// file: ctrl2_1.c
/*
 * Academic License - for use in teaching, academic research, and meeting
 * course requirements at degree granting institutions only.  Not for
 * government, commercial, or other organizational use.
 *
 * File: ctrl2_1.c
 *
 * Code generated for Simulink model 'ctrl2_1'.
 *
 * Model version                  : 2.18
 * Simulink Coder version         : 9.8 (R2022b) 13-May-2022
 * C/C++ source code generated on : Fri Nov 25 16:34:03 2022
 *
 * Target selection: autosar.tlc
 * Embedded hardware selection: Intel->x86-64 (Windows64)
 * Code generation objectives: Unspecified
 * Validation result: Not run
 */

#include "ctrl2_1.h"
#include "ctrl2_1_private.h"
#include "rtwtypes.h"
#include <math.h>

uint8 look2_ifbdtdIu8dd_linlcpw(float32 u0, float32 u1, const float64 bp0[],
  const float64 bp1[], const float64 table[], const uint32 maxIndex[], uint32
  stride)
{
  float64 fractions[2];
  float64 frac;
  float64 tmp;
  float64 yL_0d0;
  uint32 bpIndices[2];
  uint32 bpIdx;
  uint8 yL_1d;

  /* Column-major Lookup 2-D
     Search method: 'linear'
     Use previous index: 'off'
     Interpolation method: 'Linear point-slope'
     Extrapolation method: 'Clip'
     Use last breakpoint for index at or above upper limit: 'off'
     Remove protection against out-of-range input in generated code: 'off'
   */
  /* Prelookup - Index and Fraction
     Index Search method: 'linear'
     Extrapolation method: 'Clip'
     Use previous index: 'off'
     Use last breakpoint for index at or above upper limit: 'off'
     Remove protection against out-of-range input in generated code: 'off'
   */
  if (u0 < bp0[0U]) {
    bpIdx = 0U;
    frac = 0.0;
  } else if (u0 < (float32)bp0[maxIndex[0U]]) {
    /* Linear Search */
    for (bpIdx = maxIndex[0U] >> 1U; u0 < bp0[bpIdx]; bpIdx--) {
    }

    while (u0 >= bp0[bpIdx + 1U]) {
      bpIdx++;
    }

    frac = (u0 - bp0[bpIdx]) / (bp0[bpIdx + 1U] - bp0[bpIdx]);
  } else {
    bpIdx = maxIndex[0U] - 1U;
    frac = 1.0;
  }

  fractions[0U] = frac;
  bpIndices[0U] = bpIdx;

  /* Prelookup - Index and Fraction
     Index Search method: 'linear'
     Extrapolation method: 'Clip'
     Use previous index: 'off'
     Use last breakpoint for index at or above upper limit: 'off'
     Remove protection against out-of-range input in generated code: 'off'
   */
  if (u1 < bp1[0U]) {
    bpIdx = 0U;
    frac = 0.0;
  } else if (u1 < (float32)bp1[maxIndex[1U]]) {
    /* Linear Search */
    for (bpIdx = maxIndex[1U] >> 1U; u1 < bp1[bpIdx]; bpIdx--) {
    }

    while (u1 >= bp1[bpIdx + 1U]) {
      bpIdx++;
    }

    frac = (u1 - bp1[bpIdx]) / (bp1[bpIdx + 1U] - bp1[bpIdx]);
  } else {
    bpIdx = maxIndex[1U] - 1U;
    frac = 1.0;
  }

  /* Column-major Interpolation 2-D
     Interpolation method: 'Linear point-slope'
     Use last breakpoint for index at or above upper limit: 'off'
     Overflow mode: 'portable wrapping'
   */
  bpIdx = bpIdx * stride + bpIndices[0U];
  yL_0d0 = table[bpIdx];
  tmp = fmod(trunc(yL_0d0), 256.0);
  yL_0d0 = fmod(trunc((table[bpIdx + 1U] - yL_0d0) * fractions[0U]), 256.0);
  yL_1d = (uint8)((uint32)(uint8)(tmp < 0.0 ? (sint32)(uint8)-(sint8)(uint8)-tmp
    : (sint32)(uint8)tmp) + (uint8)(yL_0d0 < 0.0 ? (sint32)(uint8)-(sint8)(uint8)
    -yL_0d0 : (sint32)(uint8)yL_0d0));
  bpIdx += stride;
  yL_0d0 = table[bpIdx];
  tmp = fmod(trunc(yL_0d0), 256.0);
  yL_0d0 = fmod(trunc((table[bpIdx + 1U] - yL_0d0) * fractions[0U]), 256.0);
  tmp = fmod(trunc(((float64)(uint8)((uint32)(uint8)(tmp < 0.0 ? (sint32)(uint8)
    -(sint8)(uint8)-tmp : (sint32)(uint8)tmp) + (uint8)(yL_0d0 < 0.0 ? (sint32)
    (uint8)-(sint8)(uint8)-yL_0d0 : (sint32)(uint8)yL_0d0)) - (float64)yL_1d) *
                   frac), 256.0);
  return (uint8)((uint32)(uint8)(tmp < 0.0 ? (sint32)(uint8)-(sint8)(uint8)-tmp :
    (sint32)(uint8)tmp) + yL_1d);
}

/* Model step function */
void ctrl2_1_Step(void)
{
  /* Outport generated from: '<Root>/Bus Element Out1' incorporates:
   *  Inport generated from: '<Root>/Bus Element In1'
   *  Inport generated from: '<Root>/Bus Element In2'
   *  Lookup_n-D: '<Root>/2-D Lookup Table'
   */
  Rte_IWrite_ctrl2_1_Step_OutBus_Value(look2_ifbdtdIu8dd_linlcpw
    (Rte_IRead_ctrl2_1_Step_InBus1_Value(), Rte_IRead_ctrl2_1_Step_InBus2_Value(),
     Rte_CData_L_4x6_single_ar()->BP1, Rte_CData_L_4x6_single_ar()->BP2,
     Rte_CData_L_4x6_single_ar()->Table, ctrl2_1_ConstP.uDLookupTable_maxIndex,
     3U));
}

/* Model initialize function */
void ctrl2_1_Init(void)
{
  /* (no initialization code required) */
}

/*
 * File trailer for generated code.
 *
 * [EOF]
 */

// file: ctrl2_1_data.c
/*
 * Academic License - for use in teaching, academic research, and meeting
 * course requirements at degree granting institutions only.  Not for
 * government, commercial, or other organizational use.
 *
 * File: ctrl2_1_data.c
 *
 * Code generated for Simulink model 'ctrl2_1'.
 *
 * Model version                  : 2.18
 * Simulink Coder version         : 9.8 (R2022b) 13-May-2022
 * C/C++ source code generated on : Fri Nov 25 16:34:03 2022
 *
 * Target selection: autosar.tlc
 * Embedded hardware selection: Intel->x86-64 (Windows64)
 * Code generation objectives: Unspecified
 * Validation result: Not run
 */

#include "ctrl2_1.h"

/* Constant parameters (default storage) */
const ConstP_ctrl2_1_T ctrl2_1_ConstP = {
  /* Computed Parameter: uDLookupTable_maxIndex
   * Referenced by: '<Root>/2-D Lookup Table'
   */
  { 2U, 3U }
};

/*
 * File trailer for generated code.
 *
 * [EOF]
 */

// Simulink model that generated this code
simulink model "ctrl2_1"  (R2022b)
settings: Solver=FixedStepDiscrete  StartTime=0.0  StopTime=10.0  FixedStep=0.2  RelTol=1e-3  EnableMultiTasking=on
model workspace (MATLAB code in the model file):
  | function importfile(fileToRead1)
  | %IMPORTFILE(FILETOREAD1)
  | %  Imports data from the specified file
  | %  FILETOREAD1:  file to read
  | 
  | %  Auto-generated by MATLAB on 11-Jul-2022 12:15:19
  | 
  | % Import the file
  | newData1 = load('-mat', fileToRead1);
  | 
  | % Create new variables in the base workspace from those fields.
  | vars = fieldnames(newData1);
  | for i = 1:length(vars)
  |     assignin('base', vars{i}, newData1.(vars{i}));
  | end

== system ctrl2_1 ==
  note: Model AUTOSAR Software Components
  Bus Element In1 : Inport  PortName=InBus1  Element=Value
  Bus Element In2 : Inport  Port=2  PortName=InBus2  Element=Value
  2-D Lookup Table : Lookup_n-D  DataSpecification=Lookup table object  LookupTableObject=my2d_LkupTbl  BreakpointsForDimension1=[1:3]  BreakpointsForDimension2=[1:4]  IndexSearchMethod=Linear search  Table=[2 3 4 5; 3 4 5 6 ; 4 5 6 7]  ExtrapMethod=Clip  InternalRulePriority=Speed  OutMin=[0]  OutMax=[200]  OutDataTypeStr=uint8  RndMeth=Simplest
  Bus Element Out1 : Outport  PortName=OutBus  Element=Value
  wires:
  2-D Lookup Table/1 -> Bus Element Out1/1
  Bus Element In1/1 -> 2-D Lookup Table/1
  Bus Element In2/1 -> 2-D Lookup Table/2
